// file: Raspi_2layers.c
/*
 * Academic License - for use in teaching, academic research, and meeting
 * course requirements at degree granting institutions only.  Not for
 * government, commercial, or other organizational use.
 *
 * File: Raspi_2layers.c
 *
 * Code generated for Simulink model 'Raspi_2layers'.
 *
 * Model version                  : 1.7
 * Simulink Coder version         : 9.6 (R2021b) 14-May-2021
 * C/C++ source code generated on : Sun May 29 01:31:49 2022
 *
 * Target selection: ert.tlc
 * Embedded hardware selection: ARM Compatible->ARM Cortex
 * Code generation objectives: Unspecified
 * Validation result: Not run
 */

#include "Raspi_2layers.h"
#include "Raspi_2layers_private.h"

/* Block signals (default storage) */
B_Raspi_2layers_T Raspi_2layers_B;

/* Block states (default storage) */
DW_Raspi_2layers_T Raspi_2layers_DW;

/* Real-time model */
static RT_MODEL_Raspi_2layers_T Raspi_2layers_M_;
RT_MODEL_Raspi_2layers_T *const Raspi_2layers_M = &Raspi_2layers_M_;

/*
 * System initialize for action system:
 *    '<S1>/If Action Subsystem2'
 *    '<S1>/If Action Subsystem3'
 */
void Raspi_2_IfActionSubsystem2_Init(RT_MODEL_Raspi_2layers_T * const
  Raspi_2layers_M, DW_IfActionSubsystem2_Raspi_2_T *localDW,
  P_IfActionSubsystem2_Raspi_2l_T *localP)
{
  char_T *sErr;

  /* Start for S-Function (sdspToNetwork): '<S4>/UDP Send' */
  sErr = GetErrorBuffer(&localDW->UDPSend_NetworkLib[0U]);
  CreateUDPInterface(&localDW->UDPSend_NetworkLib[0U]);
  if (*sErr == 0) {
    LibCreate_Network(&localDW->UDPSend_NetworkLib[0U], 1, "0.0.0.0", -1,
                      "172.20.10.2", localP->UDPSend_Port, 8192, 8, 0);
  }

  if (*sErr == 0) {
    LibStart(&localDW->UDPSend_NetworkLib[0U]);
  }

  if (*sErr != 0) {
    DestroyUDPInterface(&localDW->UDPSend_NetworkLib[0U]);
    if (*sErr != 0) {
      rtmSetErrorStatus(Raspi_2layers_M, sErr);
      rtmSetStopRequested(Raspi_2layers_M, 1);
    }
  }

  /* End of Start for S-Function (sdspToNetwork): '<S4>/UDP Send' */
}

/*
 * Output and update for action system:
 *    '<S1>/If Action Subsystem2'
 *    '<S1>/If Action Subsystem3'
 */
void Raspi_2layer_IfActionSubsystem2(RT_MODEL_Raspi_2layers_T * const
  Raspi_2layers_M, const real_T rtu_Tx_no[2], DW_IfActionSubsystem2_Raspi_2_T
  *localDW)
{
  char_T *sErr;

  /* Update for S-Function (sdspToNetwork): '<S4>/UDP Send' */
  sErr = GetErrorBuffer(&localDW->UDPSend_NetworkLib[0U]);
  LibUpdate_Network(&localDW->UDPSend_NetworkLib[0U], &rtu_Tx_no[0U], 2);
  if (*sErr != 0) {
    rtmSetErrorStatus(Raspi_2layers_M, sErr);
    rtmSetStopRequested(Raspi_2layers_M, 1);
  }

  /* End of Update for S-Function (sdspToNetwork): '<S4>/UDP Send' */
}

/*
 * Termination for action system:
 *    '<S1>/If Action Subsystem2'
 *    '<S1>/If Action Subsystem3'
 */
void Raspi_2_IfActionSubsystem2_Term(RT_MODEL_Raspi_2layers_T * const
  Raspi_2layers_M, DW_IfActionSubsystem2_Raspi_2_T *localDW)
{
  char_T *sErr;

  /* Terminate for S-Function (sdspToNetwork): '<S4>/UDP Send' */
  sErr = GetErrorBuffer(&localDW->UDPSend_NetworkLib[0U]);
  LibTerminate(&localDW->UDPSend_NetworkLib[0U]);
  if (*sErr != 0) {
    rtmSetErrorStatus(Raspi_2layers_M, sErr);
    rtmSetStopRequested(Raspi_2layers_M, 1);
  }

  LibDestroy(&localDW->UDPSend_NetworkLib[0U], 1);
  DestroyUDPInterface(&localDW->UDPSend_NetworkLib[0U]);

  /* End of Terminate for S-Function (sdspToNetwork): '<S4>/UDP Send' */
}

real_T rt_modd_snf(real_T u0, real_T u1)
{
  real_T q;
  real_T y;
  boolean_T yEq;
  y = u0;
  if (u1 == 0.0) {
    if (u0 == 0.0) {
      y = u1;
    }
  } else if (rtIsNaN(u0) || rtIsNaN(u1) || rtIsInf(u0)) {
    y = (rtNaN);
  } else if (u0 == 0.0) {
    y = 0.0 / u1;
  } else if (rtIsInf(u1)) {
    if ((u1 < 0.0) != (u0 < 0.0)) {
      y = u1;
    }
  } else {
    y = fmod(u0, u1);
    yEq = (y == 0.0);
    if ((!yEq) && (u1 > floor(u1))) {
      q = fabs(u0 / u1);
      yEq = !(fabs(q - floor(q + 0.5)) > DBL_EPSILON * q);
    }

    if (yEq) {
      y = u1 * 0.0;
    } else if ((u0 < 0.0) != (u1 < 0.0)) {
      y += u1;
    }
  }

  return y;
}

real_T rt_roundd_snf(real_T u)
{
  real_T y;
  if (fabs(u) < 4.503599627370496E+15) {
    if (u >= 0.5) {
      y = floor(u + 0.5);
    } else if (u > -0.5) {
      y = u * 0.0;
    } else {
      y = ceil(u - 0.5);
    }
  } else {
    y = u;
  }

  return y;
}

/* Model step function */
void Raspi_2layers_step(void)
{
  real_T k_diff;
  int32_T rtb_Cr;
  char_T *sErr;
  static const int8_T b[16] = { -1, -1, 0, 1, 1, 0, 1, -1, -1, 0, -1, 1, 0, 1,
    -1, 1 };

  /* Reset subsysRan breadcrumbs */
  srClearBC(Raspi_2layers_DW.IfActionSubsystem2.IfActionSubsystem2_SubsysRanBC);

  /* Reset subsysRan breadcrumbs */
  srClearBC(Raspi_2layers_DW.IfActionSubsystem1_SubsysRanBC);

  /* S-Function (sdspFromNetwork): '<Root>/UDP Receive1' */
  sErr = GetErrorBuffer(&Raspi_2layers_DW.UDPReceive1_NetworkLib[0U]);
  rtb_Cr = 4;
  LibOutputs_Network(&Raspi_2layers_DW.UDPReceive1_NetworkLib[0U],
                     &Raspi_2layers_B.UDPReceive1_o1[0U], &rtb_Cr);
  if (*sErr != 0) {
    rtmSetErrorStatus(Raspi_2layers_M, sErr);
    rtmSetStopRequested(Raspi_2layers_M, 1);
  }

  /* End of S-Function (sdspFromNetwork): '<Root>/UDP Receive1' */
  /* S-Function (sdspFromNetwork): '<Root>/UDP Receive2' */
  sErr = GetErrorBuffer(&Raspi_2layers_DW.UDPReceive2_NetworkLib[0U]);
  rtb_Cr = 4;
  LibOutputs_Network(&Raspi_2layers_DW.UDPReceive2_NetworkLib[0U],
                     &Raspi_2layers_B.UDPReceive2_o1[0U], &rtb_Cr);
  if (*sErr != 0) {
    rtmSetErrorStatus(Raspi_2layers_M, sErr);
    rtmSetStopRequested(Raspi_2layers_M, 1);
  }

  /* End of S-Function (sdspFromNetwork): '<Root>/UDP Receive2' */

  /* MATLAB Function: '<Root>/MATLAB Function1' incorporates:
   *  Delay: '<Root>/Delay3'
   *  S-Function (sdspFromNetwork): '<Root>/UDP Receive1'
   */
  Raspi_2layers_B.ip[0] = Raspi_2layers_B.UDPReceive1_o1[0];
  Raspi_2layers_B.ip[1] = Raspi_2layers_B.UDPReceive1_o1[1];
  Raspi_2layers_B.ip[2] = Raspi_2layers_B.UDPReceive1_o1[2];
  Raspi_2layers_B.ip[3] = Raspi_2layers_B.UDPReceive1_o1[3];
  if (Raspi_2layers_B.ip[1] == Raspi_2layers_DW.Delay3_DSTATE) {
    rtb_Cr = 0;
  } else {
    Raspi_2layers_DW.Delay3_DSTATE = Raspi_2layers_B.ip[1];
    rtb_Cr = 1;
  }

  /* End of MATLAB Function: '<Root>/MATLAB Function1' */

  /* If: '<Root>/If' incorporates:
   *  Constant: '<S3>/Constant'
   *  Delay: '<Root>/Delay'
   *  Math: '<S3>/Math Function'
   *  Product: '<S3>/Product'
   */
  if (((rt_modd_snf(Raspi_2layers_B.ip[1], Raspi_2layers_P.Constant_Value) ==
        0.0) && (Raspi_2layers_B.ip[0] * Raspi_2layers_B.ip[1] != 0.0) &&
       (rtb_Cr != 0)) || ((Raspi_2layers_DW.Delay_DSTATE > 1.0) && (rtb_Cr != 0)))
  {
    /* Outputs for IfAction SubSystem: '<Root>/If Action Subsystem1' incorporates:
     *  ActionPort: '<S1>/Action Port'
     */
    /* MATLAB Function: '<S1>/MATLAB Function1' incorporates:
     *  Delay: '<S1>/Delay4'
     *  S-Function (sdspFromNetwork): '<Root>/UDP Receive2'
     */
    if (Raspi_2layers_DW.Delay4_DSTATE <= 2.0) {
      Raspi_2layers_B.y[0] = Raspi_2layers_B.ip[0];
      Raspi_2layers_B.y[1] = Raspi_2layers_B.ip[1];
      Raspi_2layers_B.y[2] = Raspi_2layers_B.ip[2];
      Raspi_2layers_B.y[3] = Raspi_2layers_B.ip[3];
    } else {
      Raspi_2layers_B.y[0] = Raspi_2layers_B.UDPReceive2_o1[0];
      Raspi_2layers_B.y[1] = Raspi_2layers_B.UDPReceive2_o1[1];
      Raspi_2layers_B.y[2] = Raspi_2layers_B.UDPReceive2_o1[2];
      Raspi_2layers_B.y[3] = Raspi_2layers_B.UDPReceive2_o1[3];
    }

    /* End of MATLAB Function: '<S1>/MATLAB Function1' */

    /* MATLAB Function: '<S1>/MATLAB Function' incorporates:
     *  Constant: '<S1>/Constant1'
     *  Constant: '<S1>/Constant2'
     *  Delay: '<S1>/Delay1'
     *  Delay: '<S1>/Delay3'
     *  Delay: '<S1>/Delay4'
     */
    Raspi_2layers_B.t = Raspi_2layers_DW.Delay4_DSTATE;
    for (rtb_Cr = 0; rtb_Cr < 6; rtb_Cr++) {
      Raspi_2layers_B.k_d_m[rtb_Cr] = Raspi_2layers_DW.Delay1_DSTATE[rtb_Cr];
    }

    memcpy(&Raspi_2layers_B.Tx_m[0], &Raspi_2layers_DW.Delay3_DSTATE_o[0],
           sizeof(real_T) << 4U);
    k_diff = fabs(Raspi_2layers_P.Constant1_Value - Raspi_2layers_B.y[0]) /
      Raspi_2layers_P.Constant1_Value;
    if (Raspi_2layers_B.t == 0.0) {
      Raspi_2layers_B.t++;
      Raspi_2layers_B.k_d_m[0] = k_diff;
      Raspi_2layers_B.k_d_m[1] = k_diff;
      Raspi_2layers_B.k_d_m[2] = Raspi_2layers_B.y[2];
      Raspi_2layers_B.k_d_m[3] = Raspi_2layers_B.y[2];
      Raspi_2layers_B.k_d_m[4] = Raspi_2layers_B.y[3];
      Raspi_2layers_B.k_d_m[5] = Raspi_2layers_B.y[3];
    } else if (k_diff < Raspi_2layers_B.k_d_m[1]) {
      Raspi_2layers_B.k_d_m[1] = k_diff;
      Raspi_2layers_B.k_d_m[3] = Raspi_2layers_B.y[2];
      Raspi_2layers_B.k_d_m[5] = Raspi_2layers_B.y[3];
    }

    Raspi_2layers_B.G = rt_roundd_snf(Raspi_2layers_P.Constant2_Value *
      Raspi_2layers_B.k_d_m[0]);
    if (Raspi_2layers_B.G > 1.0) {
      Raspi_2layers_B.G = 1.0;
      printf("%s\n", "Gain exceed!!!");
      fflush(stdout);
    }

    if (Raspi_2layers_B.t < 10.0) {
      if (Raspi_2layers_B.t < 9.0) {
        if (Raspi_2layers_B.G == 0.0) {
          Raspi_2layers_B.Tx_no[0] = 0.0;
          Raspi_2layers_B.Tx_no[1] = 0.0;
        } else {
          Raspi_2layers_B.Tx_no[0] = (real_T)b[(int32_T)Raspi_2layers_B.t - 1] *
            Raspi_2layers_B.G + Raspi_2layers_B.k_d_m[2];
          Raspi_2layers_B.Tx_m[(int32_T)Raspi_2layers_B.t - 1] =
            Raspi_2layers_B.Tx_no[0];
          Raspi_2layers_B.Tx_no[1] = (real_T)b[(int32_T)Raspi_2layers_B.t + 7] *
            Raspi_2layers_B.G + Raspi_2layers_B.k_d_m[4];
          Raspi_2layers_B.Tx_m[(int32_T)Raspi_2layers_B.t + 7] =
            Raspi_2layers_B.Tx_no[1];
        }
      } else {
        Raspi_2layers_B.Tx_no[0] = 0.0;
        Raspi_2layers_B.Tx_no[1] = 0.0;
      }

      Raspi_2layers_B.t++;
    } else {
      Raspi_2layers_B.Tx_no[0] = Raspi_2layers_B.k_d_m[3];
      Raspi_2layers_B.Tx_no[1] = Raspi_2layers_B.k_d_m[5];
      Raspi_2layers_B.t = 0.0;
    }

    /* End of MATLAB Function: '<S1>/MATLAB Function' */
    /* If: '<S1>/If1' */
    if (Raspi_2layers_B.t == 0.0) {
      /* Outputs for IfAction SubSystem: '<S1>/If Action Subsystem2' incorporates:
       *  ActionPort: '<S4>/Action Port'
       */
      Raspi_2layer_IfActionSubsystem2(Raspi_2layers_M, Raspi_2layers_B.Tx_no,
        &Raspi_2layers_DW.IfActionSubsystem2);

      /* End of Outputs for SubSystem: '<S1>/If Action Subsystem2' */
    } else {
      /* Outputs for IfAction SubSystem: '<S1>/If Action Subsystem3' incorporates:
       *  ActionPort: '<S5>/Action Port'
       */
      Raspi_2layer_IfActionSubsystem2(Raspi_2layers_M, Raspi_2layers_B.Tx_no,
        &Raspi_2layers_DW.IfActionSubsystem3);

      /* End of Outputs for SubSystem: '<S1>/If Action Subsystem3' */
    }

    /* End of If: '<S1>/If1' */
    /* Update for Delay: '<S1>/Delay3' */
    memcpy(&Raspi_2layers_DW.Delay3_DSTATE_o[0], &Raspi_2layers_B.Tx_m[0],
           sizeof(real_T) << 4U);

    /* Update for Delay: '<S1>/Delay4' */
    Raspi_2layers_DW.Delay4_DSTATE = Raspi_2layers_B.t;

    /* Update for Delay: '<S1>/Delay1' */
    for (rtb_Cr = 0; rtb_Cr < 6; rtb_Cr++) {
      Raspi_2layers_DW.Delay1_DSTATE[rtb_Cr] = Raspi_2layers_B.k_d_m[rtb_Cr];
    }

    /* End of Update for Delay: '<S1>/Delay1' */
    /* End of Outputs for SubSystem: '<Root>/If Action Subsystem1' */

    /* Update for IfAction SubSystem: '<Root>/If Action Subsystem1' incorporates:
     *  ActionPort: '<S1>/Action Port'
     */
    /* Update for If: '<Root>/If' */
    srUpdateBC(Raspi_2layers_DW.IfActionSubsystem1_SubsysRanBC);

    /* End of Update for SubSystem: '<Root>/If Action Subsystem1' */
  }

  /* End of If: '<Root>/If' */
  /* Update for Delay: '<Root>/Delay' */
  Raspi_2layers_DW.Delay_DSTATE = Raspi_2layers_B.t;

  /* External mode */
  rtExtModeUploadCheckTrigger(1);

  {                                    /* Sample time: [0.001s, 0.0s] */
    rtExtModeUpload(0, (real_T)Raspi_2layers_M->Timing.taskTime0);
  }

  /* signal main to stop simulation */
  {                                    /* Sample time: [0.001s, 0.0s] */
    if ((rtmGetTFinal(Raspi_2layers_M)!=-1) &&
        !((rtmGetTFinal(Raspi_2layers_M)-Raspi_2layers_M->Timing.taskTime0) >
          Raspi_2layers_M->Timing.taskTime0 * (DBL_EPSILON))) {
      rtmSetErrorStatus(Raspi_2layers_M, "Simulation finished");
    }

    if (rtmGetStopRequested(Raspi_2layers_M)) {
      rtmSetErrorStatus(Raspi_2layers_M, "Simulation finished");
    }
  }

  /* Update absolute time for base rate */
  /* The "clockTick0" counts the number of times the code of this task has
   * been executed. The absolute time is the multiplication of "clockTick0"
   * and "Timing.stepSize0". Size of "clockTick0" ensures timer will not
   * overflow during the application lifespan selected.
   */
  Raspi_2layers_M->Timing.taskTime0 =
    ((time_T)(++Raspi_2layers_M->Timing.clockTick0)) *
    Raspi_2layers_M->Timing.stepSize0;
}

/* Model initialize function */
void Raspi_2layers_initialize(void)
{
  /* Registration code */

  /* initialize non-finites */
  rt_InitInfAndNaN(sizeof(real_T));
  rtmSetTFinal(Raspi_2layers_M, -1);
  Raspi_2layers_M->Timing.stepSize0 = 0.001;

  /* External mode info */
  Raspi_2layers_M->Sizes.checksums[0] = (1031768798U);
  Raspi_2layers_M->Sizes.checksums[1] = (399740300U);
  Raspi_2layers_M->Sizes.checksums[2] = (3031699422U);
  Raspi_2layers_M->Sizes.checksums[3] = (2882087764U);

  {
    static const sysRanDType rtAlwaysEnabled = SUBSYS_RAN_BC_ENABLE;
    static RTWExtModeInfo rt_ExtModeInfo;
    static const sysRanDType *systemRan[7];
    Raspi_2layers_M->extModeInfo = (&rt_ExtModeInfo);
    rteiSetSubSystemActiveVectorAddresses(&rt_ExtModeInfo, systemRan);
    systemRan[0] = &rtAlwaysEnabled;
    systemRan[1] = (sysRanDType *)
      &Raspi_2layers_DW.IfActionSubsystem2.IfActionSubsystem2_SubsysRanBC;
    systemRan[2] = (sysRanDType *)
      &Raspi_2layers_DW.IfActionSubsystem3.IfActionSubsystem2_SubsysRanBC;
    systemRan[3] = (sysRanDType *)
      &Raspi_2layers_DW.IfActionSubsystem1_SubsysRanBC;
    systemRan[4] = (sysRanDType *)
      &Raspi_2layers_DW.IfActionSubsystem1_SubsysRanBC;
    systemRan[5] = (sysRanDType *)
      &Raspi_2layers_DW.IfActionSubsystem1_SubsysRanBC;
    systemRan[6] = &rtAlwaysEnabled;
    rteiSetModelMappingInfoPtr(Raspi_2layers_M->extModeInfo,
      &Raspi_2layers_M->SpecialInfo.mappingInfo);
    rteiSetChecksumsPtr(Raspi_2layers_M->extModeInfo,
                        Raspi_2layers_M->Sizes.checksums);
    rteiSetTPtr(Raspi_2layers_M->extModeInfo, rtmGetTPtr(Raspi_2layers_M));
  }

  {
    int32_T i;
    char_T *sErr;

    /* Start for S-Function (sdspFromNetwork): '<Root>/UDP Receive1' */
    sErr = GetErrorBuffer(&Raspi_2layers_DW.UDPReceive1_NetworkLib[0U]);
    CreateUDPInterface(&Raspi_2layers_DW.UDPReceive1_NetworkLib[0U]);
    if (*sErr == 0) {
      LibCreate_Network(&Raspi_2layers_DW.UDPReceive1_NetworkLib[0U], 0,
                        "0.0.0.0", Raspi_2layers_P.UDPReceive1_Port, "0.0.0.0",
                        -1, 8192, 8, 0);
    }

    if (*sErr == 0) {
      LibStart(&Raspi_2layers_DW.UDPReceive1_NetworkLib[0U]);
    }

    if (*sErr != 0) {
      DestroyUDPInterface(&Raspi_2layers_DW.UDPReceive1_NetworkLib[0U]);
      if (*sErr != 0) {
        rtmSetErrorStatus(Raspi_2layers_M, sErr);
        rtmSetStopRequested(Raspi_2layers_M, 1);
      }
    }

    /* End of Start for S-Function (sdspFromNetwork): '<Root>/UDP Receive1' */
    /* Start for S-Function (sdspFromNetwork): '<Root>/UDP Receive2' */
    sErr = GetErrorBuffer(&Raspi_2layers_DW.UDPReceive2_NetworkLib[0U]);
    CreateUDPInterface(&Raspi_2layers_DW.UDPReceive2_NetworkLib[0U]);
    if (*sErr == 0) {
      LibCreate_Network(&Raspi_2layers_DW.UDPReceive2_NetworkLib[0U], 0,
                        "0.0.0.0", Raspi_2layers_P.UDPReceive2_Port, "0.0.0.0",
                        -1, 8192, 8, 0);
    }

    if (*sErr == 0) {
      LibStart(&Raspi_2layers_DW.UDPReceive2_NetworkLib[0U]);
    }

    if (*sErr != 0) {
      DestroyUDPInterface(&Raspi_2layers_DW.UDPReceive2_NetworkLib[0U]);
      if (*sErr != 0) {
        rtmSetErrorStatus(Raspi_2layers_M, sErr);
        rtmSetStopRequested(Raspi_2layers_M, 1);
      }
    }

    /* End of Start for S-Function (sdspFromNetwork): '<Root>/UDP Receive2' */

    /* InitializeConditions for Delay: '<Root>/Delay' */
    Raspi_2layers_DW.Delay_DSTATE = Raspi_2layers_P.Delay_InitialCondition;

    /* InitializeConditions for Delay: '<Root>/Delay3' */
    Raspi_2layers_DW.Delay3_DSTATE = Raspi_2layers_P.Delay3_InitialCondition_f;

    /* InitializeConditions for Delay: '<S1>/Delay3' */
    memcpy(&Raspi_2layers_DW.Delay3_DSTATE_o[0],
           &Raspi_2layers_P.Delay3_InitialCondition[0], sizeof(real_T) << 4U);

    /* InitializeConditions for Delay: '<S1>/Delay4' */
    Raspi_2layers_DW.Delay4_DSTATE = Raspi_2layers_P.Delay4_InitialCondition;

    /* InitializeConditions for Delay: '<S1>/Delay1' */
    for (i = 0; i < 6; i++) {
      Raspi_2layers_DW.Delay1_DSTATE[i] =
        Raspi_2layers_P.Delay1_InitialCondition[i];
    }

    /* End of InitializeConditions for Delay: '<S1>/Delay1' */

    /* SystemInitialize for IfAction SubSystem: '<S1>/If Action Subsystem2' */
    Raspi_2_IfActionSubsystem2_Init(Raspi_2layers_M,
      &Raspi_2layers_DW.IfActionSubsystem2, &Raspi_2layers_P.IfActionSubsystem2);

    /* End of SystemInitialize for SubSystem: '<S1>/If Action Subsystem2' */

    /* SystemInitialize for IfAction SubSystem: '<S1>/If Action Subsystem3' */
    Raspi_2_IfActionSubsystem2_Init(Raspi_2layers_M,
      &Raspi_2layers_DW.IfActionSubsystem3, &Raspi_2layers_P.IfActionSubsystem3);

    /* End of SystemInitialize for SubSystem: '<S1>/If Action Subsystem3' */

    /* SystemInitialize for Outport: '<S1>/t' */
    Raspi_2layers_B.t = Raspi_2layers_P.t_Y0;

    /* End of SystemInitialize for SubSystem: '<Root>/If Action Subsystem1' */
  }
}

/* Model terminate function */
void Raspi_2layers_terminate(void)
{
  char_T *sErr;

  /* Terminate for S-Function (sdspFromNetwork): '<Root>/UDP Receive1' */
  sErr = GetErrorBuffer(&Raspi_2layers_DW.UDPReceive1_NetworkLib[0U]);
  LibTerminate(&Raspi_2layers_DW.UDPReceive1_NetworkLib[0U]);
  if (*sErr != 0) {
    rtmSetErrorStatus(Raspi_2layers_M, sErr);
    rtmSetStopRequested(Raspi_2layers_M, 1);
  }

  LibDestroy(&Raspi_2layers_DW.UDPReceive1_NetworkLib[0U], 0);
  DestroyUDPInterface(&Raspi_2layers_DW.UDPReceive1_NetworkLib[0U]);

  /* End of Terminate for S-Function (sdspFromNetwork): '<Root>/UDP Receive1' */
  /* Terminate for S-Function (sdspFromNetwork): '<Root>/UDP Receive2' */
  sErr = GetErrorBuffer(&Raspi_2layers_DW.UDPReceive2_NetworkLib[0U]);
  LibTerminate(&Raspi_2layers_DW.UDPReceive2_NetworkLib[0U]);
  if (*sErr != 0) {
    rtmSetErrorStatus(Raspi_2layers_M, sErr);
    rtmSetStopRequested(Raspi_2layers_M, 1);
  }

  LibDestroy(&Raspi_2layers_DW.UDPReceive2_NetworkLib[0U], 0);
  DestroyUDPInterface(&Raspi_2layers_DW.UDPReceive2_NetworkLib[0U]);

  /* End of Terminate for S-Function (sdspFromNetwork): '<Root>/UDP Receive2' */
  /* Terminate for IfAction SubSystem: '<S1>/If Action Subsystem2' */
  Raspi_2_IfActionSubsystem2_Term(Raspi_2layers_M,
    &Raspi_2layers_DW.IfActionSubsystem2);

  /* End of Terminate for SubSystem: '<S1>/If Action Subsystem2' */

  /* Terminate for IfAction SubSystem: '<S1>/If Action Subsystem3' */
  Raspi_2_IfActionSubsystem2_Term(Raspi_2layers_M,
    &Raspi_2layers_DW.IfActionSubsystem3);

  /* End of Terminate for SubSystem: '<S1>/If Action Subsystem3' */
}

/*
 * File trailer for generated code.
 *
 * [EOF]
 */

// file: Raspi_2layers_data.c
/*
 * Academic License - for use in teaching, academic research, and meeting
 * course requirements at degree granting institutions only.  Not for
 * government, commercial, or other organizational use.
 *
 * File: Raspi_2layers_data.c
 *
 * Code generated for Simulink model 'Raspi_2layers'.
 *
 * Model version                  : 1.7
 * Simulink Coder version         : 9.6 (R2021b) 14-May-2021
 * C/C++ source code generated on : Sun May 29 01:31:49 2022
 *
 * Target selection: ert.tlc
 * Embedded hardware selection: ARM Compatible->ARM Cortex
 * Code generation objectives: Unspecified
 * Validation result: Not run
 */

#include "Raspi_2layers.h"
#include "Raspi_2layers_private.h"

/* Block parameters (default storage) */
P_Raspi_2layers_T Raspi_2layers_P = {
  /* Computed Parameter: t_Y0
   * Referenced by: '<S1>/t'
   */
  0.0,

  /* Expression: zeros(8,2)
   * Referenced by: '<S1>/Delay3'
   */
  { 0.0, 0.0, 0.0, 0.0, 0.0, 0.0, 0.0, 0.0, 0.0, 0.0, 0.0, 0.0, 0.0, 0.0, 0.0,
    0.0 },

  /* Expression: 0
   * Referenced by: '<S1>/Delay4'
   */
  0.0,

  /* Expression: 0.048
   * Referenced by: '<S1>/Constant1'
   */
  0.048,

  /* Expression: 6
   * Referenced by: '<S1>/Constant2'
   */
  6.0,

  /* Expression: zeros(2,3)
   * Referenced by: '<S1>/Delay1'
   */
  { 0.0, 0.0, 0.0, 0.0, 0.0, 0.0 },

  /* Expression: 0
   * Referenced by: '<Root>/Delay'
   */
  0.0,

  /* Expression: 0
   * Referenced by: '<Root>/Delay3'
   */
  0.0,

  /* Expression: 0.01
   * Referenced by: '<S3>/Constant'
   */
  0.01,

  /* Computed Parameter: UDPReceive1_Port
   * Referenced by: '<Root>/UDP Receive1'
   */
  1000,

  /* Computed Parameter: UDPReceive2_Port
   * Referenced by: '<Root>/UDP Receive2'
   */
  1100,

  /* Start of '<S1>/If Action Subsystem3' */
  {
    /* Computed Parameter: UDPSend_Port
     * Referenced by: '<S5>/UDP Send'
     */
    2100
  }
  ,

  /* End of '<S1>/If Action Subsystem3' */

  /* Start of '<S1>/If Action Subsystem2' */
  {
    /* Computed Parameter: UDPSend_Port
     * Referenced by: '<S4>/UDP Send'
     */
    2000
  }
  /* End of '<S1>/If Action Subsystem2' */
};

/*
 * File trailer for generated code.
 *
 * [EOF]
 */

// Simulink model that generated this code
simulink model "Raspi_2layers"  (R2021b)
settings: Solver=FixedStepDiscrete  StartTime=0.0  StopTime=inf  FixedStep=1e-2  RelTol=1e-3  EnableMultiTasking=on
libraries: raspberrypiNetworklib x4

== system Raspi_2layers ==
  Delay : Delay  DelayLength=1  InitialCondition=0
  Delay3 : Delay  DelayLength=1  InitialCondition=0
  Display6 : Display
  If : If  NumInputs=4  IfExpression=(u1 == 0 & u2 ~=0& u4~=0) | (u3 > 1& u4~=0)  ShowElse=off
  If Action Subsystem1 : Subsystem  TreatAsAtomicUnit=on
  MATLAB Function1 : MATLAB Function  TreatAsAtomicUnit=on
  UDP Receive1 : raspberrypiNetworklib/UDP Receive  localURL='0.0.0.0'  localPort=1000  remoteURL='0.0.0.0'  remotePort=-1  recvBufferSize=8192  signalDatatype=double  dims=4  isVarSize=off  showBlockingTime=off  blockingTime=0  sampletime=-1  blockPlatform=Raspberry Pi
  UDP Receive2 : raspberrypiNetworklib/UDP Receive  localURL='0.0.0.0'  localPort=1100  remoteURL='0.0.0.0'  remotePort=-1  recvBufferSize=8192  signalDatatype=double  dims=4  isVarSize=off  showBlockingTime=off  blockingTime=0  sampletime=-1  blockPlatform=Raspberry Pi
  trigger : Subsystem
  wires:
  MATLAB Function1/1(Cr) -> If/4
  trigger/1(mod) -> If/1
  Delay3/1 -> MATLAB Function1/2("ip_pre ")
  UDP Receive1/1 -> Display6/1, MATLAB Function1/1("ip ")
  trigger/2(And) -> If/2
  MATLAB Function1/2(ip) -> If Action Subsystem1/1(ip), trigger/1(ip)
  Delay/1 -> If/3
  MATLAB Function1/3(ip_pre) -> Delay3/1
  If Action Subsystem1/1(t) -> Delay/1
  UDP Receive2/1 -> If Action Subsystem1/2(ip1)
  If/1 -> If Action Subsystem1/Action

== system Raspi_2layers/If Action Subsystem1 ==
  ip : Inport
  ip1 : Inport  Port=2
  Action Port : ActionPort  ActionPortLabel=if((u1 == 0 & u2 ~=0& u4~=0) | (u3 > 1& u4~=0))
  Constant1 : Constant  Value=2.88e-2
  Constant2 : Constant  Value=6
  Delay1 : Delay  DelayLength=1  InitialCondition=zeros(2,3)
  Delay3 : Delay  DelayLength=1  InitialCondition=zeros(8,2)
  Delay4 : Delay  DelayLength=1  InitialCondition=0
  Display{1..8} (8 alike) : Display
  If Action Subsystem2 : Subsystem  TreatAsAtomicUnit=on
  If Action Subsystem3 : Subsystem  TreatAsAtomicUnit=on
  If1 : If  IfExpression=u1 == 0
  MATLAB Function : MATLAB Function  TreatAsAtomicUnit=on
  MATLAB Function1 : MATLAB Function  TreatAsAtomicUnit=on
  Selector : Selector  InputPortWidth=4  IndexOptions=Index vector (dialog)  Indices=1  OutputSizes=1
  Selector1 : Selector  InputPortWidth=4  IndexOptions=Index vector (dialog)  Indices=[3;4]  OutputSizes=1
  t : Outport
  wires:
  MATLAB Function/5(Tx_m) -> Display5/1, Delay3/1
  MATLAB Function/2(G) -> Display4/1
  MATLAB Function/4(k_d_m) -> Delay1/1, Display2/1
  Delay1/1 -> MATLAB Function/6("k_d_m ")
  Selector/1 -> Display3/1, MATLAB Function/1(k)
  MATLAB Function/3(t) -> If1/1, Display7/1, Delay4/1, t/1
  Delay4/1 -> MATLAB Function1/3(t), MATLAB Function/5("t ")
  MATLAB Function/1(Tx_no) -> If Action Subsystem3/1(Tx_no), If Action Subsystem2/1(Tx_no), Display1/1
  Constant2/1 -> MATLAB Function/4(amp)
  Selector1/1 -> MATLAB Function/2(Tx_pre)
  Delay3/1 -> MATLAB Function/7("Tx_m ")
  MATLAB Function1/1(y) -> Selector1/1, Selector/1
  Constant1/1 -> MATLAB Function/3(k_opt)
  ip/1 -> MATLAB Function1/1(u), Display6/1
  If1/1 -> If Action Subsystem2/Action
  If1/2 -> If Action Subsystem3/Action
  ip1/1 -> Display8/1, MATLAB Function1/2(v)

== system Raspi_2layers/trigger ==
  ip : Inport
  Cast To Double : DataTypeConversion  OutDataTypeStr=double
  Constant : Constant  Value=0.01
  Display : Display
  Math Function : Math  Operator=mod  SaturateOnIntegerOverflow=on
  Product : Product
  Selector : Selector  InputPortWidth=4  IndexOptions=Index vector (dialog)  Indices=2  OutputSizes=1
  Selector1 : Selector  InputPortWidth=4  IndexOptions=Index vector (dialog)  Indices=1  OutputSizes=1
  mod : Outport
  And : Outport  Port=2
  wires:
  Constant/1 -> Math Function/2
  Selector/1 -> Display/1, Product/1, Math Function/1
  ip/1 -> Selector1/1, Selector/1
  Math Function/1 -> mod/1
  Product/1 -> Cast To Double/1
  Selector1/1 -> Product/2
  Cast To Double/1 -> And/1

== system Raspi_2layers/If Action Subsystem1/If Action Subsystem2 ==
  Tx_no : Inport
  Action Port : ActionPort  ActionPortLabel=if(u1 == 0)
  UDP Send : raspberrypiNetworklib/UDP Send  remoteURL='172.20.10.2'  remotePort=2000  localURL='0.0.0.0'  localPortSource=Automatically determine  localPort=-1  sampletime=-1  blockPlatform=Raspberry Pi  separateLengthPort=0
  wires:
  Tx_no/1 -> UDP Send/1

== system Raspi_2layers/If Action Subsystem1/If Action Subsystem3 ==
  Tx_no : Inport
  Action Port : ActionPort  ActionPortLabel=else
  UDP Send : raspberrypiNetworklib/UDP Send  remoteURL='172.20.10.2'  remotePort=2100  localURL='0.0.0.0'  localPortSource=Automatically determine  localPort=-1  sampletime=-1  blockPlatform=Raspberry Pi  separateLengthPort=0
  wires:
  Tx_no/1 -> UDP Send/1

== matlab function Raspi_2layers/MATLAB Function1 ==
function [Cr,ip, ip_pre] = fcn(ip, ip_pre)

ip2 = ip(2);

if ip2 == ip_pre
    Cr = 0;
else
    ip_pre = ip2;
    Cr = 1;

end

== matlab function Raspi_2layers/If Action Subsystem1/MATLAB Function1 ==
function y = IpSelector(u,v,t)
if t<=2
    y = u;
else
    y = v;
end

== matlab function Raspi_2layers/If Action Subsystem1/MATLAB Function ==
function [Tx_no,G,t,k_d_m,Tx_m] = Controller(k,Tx_pre,k_opt,amp,t,k_d_m,Tx_m)

k_diff = abs(k_opt-k)/k_opt;
Tx_pre = Tx_pre';

if t == 0
   

    t = t+1;
    k_d_m(1,:)  = [k_diff,Tx_pre];
    k_d_m(2,:)  = [k_diff,Tx_pre];

    
else

    if k_diff < k_d_m(2,1)

       k_d_m(2,:)  = [k_diff,Tx_pre];

    end

end

G = round(amp*k_d_m(1,1));  
Tx_fix = k_d_m(1,2:3)';

if G >1
    G =1;
    disp("Gain exceed!!!")
end

if t < 10
    
    if t < 9

        if G ==0
            Tx_no = [0;0];
        else

            dir_att = [-1,-1; -1,0; 0,-1; 1,1; 1,0; 0,1; 1,-1; -1,1];
            
            
            Tx_no =G*dir_att(t,:)'+Tx_fix;
        
            Tx_m (t,:) = Tx_no;
        end

    else

         Tx_no = [0;0]; % off

    end

    t =t+1;

else
    
    
    Tx_no = k_d_m(2,2:3)';

    t =0;
   
 
end
